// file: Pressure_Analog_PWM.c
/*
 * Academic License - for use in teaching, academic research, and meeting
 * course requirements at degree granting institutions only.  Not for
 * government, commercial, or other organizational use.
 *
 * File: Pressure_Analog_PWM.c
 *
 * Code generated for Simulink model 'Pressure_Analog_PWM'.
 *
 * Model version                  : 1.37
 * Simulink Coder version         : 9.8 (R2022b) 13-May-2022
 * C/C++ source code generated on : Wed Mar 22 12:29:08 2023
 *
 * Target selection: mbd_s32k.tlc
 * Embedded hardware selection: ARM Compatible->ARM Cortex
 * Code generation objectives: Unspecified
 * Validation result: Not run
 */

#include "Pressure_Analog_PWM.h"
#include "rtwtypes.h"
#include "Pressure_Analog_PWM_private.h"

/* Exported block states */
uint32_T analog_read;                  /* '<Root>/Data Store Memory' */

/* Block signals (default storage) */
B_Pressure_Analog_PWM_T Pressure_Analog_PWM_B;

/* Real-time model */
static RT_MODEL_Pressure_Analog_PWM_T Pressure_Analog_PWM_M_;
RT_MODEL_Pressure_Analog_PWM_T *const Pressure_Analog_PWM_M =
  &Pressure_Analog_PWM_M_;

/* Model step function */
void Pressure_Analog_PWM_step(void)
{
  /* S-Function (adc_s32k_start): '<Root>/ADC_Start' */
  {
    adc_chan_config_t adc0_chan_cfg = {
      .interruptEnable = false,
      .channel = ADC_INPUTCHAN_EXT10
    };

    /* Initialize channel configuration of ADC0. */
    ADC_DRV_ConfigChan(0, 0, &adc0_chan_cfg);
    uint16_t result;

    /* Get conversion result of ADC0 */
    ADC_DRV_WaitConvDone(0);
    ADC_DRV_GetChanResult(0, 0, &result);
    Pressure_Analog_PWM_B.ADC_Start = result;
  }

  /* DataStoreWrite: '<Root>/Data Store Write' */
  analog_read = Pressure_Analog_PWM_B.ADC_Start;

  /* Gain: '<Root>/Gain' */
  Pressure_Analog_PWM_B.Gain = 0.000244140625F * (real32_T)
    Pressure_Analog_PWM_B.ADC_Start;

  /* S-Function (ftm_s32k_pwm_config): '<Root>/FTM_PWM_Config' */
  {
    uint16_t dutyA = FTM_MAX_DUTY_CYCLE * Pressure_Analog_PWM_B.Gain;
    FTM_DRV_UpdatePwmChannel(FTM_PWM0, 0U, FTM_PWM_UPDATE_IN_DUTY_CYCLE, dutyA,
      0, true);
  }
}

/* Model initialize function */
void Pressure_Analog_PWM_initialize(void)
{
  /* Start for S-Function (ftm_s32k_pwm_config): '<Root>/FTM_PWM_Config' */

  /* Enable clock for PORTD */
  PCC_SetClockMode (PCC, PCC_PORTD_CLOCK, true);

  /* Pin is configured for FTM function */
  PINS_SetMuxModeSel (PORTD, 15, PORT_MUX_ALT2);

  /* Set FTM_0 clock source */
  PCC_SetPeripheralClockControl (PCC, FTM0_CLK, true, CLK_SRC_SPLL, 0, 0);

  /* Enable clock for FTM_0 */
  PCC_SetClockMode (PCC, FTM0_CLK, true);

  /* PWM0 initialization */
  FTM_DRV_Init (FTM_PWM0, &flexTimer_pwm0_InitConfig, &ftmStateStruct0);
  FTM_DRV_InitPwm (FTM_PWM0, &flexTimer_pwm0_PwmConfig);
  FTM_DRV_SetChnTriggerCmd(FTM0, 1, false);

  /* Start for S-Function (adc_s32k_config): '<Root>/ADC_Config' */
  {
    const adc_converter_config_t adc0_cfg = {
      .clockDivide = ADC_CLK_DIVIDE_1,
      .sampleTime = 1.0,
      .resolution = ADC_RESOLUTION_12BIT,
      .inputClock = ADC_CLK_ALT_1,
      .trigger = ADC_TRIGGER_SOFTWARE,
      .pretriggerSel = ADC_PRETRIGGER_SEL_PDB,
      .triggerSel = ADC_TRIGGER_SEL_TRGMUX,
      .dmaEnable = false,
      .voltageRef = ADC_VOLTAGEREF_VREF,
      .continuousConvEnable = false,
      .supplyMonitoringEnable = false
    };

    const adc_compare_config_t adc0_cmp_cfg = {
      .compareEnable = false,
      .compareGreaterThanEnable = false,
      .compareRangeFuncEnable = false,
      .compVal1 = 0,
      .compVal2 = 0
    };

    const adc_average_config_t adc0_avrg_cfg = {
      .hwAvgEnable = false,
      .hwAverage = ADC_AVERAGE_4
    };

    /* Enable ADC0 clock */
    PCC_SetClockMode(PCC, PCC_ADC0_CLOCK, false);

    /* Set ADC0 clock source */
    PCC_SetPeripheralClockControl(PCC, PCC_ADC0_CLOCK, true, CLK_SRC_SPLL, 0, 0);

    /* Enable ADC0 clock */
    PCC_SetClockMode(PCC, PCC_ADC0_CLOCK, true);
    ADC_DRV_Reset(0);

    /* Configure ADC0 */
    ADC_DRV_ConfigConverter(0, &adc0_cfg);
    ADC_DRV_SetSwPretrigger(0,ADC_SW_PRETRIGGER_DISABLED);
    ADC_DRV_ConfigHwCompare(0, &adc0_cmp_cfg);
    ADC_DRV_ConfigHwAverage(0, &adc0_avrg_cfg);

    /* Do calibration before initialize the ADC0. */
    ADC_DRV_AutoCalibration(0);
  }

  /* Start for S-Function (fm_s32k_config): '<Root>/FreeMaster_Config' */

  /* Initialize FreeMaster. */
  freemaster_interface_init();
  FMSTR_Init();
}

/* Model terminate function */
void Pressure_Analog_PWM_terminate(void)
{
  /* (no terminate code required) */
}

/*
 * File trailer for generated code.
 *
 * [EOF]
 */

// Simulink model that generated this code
simulink model "Pressure_Analog_PWM"  (R2022b)
settings: Solver=FixedStepDiscrete  StartTime=0.0  StopTime=10.0  RelTol=1e-3  EnableMultiTasking=on
InitFcn:
  | mbd_s32k_consistency_checks(bdroot(gcs));
model workspace (MAT data in the model file):
  mwTaskManagerKernelLatency = 1e-06
undefined symbols (not defined in the file or in its folder): LQFP
libraries: mbd_s32k1xx_ec_toolbox x5

== system Pressure_Analog_PWM ==
  note: This algorithm reads the analog output from the pressure
      | sensor and changes the red LED intensity accordingly.
      | The read value can be visualized on FreeMaster through
      |  the variable "analog_read".
      |
      | Hardware Requirements:
      | - S32K144 board
      | - HTDM100USP
      |
      | Pin connections:
      |
      | Sensor    |     Board
      |     1         |      PTC2
      |     2         |      GND
      |     8         |        5V
      |
      |
      | Kamilla Peixoto - Scaleo Medical
      | v1 - 22/03/2023
  note: Analog Reading
  note: Watched Variables
  note: Configuration
  ADC_Config : mbd_s32k1xx_ec_toolbox/Motor Control Blocks/ADC Blocks/ADC_Config  instance=0  mode=12-bit conversion  smplts=2  adiclk=alternate clock 1  adiv=input clock  show_adv_opts=on  pretrgsel=PDB pre-trigger  swpretrg=Disabled  adtrg=software  trgsel=TRGMUX output  refsel=Vrefh and Vrefl  supply_monitoring=off  acfe=off  acfgt=off  acren=off  cv1=0  cv2=0  adco=off  avge=off  avgs=4 samples
  ADC_Start : mbd_s32k1xx_ec_toolbox/Motor Control Blocks/ADC Blocks/ADC_Start  instance=0  adc_r=A  adc_chan=PTC2: [ADC0_SE10 | ADC Single Ended Input]  aien=off  mcuTargetUpdate=on
  Data Store Memory : DataStoreMemory  DataStoreName=analog_read  WriteAfterWriteMsg=warning  ShowAdditionalParam=off  StateMustResolveToSignalObject=on
  Data Store Write : DataStoreWrite  DataStoreName=analog_read  IndexOptions=Index vector (dialog)  Indices=1  OutputSizes=1
  FTM_PWM_Config : mbd_s32k1xx_ec_toolbox/Motor Control Blocks/FTM Blocks/FTM_PWM_Config  ftmModule=0  ftmMode=Edge-Aligned PWM  ftmSourceClock=80 MHz  swcontrol_enable=off  chan0En=on  chan0Type=Complementary  chan2En=off  chan2Type=Independent  chan4En=off  chan4Type=Independent  chan6En=off  chan6Type=Independent  ftmPwmUnits=Hz  outFrequency=10000  ftmPeriod=8000  ftmPrescaler=Divide by 1  deadtimeUnits=Nanoseconds  deadtimeNs=0  deadtimeTicks=0  deadtimePrescaler=Divide by 1  dutyCycleCh0=0.25  dutyCycleCh1=0.25  dutyCycleCh2=0.25  dutyCycleCh3=0.25  dutyCycleCh4=0.25  dutyCycleCh5=0.25  dutyCycleCh6=0.25  dutyCycleCh7=0.25  dutyCycleSim=off  startAfterInit=on  showAdvOpt=on  pinFtmCh0=PTD15: [FTM0_CH0 | FTM Channel]  pinFtmCh1=None  pinPolCh0=Active Low  pinPolCh1=Active Low  outputComplem0=Main duplicated  outputLevel0=Low  outputLevel1=Low  pinFtmCh2=PTD0: [FTM0_CH2 | FTM Channel]  pinFtmCh3=None  pinPolCh2=Active Low  pinPolCh3=Active Low  outputComplem2=Main duplicated  outputLevel2=Low  outputLevel3=Low  pinFtmCh4=PTB4: [FTM0_CH4 | FTM Channel]  pinFtmCh5=None  pinPolCh4=Active Low  pinPolCh5=Active Low  outputComplem4=Main duplicated  outputLevel4=Low  outputLevel5=Low  pinFtmCh6=PTA17: [FTM0_CH6 | FTM Channel]  pinFtmCh7=None  pinPolCh6=Active Low  pinPolCh7=Active Low  outputComplem6=Main duplicated  outputLevel6=Low  outputLevel7=Low  initTrigger=off  chTrigger0=off  chTrigger1=off  chTrigger2=off  chTrigger3=off  chTrigger4=off  chTrigger5=off  chTrigger6=off  chTrigger7=off  mcuTargetUpdate=on  pwmSyncTrg=Software trigger  pwmSyncHwRouting=TRGMUX_FTM7  pwmSyncTrg0=off  pwmSyncTrg1=off  pwmSyncTrg2=off  pwmSyncAutoClear=on  pwmSyncMinLoad=on  pwmSyncMaxLoad=on  pwmSyncInvert=System Clock  pwmSyncOutControl=System Clock  pwmSyncOutMask=System Clock  pwmSyncCounterInitial=System Clock  pwmSyncPoints=Update now  reloadEnable=off  reloadPriority=15  reloadHalfCycle=off  reloadHCR=0  reloadFrequency=0  chnMatch0=off  chnMatch1=off  chnMatch2=off  chnMatch3=off  chnMatch4=off  chnMatch5=off  chnMatch6=off  chnMatch7=off  pwmFaultProtection=off  pwmFaultInterrupt=off  pwmFaultClearing=Fault control disabled  pwmFaultPinState=Safe Value  pwmFaultFilterValue=0  pwmFaultPriority=15  fault_disen_0=off  fault_filter_0=off  fault_polarity_0=Active High  fault_disen_1=off  fault_filter_1=off  fault_polarity_1=Active high  fault_disen_2=off  fault_filter_2=off  fault_polarity_2=Active high  fault_disen_3=off  fault_filter_3=off  fault_polarity_3=Active high  fault_pin_0=None  fault_pin_1=None  fault_pin_2=None  fault_pin_3=None
  FreeMaster_Config : mbd_s32k1xx_ec_toolbox/Utility Blocks/FreeMaster_Config  interface=LPUART1  baudrate=115200  rxd=PTC6: [LPUART1_RX | Receive]  txd=PTC7: [LPUART1_TX | Transmit]  mode=Poll-driven  isr_prio=15  show_adv_opts=on  use_scope=on  max_scope_vars=8  use_recorder=on  max_rec_vars=8  rec_buff_size=1024  rec_timebase=0 seconds  comm_buffer_size_auto=on  comm_buffer_size=255  comm_rqueue_size_default=on  comm_rqueue_size=32
  Gain : Gain  Gain=2^(-12)  ParamDataTypeStr=single
  MBD_S32K14x_Config_Information : mbd_s32k1xx_ec_toolbox/MBD_S32K1xx_Config_Information  Priority=0  mbdt_ver=0  disp_str=|  config_params=[]  mcu_target_name=S32K144  mcu_target_package=100-LQFP  mcu_target_sram_size=64KB  mcu_system_clock_freq=80  mcu_xtal_freq=External 8  mcu_steptick_timer=LPIT Channel 0  mcu_steptick_prio=15  ds_import_enable=on  target_compiler=GCC  target_memory=FLASH  gcc_target_compile_opts=-mcpu=cortex-m4 -mthumb -mfloat-abi=hard -mfpu=fpv4-sp-d16 -O1 -g -gstrict-dwarf  gcc_target_assemble_opts=-mcpu=cortex-m4 -mthumb -mfloat-abi=hard -mfpu=fpv4-sp-d16 -g  gcc_target_link_opts=-mcpu=cortex-m4 -mthumb -mfloat-abi=hard -mfpu=fpv4-sp-d16  gcc_target_default_lcf=on  gcc_target_user_lcf=S32K148_192_flash.ld  ghs_target_compile_opts=-cpu=cortexm4f -thumb -DARM_MATH_CM4 -fpu=vfpv4_d16 -fsingle -Ogeneral -Wundef -Wimplicit-int -Wshadow -Wtrigraphs --no_commons --gnu_asm -gnu99 -gdwarf-2 -G  ghs_target_assemble_opts=-cpu=cortexm4f -fpu=vfpv4_d16  ghs_target_link_opts=-cpu=cortexm4f -thumb -fpu=vfpv4_d16  ghs_target_default_lcf=off  ghs_target_user_lcf=S32K148_192_flash.ld  iar_target_compile_opts=--cpu=Cortex-M4F --thumb --fpu=VFPv4_sp -Ol -e --debug --dlib_config normal  iar_target_assemble_opts=--cpu Cortex-M4F --thumb --fpu VFPv4_sp  iar_target_link_opts=--no_exceptions --vfe --inline  iar_target_default_lcf=off  iar_target_user_lcf=S32K148_192_flash.icf  pil_download_enable=off  rbl_download_enable=on  rbl_start_delay=5000000  rbl_download_interface=OpenSDA  rbl_restart_request=off  rbl_com_port=Custom  rbl_com_port_custom=COM1  pil_download_rate=57600  pil_opensda_drive=Custom  pil_opensda_drive_custom=D  pil_uart_instance=1  pil_uart_rx=PTC6: [LPUART1_RX | Receive]  pil_uart_tx=PTC7: [LPUART1_TX | Transmit]  FTM_PWM_PcrCheckEnDis=on  FTM_Input_Edge_Inputs_PcrCheckEnDis=on  FTM_Dual_Edge_Inputs_PcrCheckEnDis=on  FTM_Quadrature_Inputs_PcrCheckEnDis=on  FTM_Hall_Sensor_Inputs_PcrCheckEnDis=on  LPTMR_PcrCheckEnDis=on  PIT_PcrCheckEnDis=on  RTC_PcrCheckEnDis=on  FlexCAN_PcrCheckEnDis=on  LIN_PcrCheckEnDis=on  FlexIO_PcrCheckEnDis=on  LPI2C_PcrCheckEnDis=on  LPSPI_PcrCheckEnDis=on  LPUART_PcrCheckEnDis=on  CMP_PcrCheckEnDis=on  GPIO_OutputPcrCheckEnDis=on  GPIO_InputPcrCheckEnDis=on  SBC_PcrCheckEnDis=on  BMS_PcrCheckEnDis=on  AMMCLIB_PcrCheckEnDis=on  FM_PcrCheckEnDis=on  Profile_PcrCheckEnDis=on  ConfigParams_PcrCheckEnDis=on  ModelRef_PcrCheckEnDis=on  PDB0_PcrCheckEnDis=on  CSEc_PcrCheckEnDis=on  eDMA_PcrCheckEnDis=on  FLASH_PcrCheckEnDis=on  ADC_PcrCheckEnDis=on  WDOG_PcrCheckEnDis=on
      | Target : S32K144-64KB_SRAM
      | Package : 100-pin
      | System clock : 80 MHz
      | XTAL clock : External 8 MHz
      | Compiler : GCC
      | Target Type : FLASH
      | Download Code after build : (OpenSDA: E)
      | Step Tick Interrupt Priority : 15
  wires:
  ADC_Start/1 -> Data Store Write/1, Gain/1
  Gain/1 -> FTM_PWM_Config/1
